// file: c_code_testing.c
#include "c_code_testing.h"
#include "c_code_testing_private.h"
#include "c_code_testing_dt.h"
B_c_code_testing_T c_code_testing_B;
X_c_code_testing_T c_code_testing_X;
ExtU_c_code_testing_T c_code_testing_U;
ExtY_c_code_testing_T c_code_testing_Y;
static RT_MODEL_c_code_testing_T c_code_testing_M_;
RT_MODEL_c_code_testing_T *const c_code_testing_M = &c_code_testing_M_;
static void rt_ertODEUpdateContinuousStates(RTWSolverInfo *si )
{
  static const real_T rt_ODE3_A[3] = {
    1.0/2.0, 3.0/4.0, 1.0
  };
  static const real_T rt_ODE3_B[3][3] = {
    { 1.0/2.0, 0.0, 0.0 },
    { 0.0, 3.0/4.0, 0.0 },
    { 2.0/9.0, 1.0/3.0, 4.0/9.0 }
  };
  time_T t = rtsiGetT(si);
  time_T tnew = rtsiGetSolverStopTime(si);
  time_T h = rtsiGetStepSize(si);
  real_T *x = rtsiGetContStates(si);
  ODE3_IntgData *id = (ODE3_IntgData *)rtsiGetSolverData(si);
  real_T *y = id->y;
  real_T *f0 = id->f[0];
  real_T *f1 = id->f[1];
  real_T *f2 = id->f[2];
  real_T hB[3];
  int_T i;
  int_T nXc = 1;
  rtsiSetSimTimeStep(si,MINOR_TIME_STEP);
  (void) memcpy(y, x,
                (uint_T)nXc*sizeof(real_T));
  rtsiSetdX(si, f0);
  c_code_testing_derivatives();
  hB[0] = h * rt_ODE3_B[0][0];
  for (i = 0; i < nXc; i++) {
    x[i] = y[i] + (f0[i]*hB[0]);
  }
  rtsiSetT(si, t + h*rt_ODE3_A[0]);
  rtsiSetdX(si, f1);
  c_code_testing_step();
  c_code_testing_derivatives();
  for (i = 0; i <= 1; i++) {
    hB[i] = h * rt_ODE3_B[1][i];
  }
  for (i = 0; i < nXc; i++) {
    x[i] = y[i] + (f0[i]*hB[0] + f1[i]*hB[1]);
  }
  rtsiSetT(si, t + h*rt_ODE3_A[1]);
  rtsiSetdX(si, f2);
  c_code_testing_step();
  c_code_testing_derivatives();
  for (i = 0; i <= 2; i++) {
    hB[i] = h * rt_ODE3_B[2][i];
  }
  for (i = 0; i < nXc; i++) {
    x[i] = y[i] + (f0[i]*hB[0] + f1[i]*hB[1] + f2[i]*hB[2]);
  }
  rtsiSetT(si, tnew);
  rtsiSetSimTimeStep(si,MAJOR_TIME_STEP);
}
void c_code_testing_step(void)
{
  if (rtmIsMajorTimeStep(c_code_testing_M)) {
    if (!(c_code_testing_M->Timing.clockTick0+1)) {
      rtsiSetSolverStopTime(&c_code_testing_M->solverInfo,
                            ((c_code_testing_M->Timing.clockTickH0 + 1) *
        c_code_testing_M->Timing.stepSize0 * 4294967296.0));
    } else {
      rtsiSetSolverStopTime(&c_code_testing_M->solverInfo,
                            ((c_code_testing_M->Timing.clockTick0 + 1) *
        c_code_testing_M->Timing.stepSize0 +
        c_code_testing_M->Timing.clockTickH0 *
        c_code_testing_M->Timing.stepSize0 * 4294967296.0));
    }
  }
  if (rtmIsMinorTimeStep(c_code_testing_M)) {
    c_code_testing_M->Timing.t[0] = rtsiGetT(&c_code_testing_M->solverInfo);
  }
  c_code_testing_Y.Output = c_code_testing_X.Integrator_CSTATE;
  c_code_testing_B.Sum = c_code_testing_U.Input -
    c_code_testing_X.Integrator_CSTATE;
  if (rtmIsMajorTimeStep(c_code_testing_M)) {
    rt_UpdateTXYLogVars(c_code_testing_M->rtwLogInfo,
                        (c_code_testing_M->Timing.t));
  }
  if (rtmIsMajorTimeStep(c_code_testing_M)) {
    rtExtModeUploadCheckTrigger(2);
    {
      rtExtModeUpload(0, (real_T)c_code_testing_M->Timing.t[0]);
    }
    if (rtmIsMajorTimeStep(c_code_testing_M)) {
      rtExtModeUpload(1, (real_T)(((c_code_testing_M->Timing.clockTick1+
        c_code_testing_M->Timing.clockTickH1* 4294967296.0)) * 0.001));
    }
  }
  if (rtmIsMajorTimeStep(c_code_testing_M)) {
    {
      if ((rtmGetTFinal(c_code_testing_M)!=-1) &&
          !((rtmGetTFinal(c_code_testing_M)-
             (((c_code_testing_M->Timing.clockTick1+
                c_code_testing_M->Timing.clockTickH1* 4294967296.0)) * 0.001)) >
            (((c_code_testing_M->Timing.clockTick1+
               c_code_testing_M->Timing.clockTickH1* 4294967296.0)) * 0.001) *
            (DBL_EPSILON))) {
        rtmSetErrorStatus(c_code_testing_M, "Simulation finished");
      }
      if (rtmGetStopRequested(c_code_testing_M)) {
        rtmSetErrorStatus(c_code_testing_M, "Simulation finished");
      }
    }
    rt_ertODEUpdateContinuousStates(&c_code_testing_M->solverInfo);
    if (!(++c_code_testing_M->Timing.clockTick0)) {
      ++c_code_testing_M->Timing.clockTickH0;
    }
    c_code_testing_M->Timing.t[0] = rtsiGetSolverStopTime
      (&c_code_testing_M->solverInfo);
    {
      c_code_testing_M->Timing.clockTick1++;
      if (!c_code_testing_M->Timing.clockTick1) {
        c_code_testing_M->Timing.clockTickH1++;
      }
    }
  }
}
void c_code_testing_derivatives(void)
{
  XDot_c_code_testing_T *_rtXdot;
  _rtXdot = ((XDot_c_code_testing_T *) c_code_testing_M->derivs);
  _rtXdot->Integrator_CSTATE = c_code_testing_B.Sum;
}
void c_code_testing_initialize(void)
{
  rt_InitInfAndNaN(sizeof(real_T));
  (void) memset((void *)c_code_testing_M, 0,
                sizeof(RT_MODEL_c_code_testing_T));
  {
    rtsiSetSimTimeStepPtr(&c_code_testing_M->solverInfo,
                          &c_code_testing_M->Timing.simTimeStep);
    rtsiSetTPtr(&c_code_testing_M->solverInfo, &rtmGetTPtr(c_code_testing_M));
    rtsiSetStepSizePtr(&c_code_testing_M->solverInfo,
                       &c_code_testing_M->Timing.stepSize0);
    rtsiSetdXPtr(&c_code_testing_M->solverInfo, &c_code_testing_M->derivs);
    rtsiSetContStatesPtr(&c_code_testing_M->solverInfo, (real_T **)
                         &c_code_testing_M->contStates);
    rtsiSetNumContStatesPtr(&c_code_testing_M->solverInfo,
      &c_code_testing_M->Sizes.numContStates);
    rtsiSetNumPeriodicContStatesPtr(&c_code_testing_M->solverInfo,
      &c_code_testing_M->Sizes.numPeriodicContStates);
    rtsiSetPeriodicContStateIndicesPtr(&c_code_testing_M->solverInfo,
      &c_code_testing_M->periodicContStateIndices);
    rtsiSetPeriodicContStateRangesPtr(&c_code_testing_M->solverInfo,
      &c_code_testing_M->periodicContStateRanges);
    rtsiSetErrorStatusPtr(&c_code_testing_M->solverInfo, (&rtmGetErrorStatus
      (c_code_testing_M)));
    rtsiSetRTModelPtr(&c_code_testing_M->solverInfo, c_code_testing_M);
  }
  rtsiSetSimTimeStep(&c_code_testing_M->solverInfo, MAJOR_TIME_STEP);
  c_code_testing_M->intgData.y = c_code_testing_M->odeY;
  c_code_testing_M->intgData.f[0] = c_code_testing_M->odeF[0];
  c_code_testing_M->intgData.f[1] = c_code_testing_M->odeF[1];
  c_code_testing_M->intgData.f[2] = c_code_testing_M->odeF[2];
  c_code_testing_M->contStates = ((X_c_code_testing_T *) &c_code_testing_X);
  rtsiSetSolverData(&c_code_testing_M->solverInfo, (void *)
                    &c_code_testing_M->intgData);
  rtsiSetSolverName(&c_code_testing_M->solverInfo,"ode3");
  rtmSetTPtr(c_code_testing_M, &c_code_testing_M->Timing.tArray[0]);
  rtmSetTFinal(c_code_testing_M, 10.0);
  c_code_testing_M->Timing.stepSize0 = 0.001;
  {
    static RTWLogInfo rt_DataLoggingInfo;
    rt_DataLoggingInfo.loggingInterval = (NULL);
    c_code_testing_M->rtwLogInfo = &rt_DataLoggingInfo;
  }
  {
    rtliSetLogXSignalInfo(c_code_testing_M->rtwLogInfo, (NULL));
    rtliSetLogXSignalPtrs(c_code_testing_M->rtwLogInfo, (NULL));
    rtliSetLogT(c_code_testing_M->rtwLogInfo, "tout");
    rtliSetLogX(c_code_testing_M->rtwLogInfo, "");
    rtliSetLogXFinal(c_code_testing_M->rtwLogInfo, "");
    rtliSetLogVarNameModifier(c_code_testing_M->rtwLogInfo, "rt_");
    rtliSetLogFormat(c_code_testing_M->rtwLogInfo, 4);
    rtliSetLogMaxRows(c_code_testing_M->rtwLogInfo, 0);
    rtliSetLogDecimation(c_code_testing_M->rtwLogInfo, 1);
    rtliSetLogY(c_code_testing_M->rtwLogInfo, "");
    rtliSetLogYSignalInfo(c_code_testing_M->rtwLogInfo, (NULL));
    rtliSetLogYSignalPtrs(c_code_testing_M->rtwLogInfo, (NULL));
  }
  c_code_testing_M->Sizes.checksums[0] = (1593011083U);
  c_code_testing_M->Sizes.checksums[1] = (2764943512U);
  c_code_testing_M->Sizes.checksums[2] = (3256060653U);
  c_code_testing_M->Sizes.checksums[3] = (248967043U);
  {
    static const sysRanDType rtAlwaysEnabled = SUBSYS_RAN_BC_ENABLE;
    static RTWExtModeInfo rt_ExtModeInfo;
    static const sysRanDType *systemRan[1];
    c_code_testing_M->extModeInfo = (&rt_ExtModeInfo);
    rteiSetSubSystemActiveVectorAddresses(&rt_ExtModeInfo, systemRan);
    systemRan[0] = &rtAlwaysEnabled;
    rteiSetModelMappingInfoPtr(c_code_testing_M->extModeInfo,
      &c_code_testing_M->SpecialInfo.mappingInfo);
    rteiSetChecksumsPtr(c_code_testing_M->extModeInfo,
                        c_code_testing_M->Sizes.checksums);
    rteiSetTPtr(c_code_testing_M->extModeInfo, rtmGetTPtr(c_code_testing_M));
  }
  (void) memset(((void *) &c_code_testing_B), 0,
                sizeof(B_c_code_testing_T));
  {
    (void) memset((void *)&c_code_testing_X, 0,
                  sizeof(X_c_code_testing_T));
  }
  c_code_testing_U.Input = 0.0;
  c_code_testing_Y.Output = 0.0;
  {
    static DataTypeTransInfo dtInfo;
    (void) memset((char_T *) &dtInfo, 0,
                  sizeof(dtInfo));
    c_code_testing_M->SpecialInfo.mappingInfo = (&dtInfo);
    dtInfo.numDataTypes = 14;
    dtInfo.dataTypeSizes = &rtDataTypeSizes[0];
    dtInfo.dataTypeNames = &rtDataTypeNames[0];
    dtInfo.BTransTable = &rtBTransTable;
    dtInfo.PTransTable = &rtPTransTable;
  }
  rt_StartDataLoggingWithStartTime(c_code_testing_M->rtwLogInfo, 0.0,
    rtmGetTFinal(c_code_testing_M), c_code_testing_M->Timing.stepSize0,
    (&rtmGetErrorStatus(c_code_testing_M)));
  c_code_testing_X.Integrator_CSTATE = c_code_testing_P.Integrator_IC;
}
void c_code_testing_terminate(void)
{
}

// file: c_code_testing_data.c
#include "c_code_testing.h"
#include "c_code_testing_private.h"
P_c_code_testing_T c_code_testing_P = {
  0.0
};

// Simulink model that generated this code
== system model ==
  Input : Inport
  Output : Outport  <- 1: Integrator
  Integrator : Integrator  <- 1: Sum
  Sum : Sum  Inputs=+-  <- 1: Input, 2: Integrator
